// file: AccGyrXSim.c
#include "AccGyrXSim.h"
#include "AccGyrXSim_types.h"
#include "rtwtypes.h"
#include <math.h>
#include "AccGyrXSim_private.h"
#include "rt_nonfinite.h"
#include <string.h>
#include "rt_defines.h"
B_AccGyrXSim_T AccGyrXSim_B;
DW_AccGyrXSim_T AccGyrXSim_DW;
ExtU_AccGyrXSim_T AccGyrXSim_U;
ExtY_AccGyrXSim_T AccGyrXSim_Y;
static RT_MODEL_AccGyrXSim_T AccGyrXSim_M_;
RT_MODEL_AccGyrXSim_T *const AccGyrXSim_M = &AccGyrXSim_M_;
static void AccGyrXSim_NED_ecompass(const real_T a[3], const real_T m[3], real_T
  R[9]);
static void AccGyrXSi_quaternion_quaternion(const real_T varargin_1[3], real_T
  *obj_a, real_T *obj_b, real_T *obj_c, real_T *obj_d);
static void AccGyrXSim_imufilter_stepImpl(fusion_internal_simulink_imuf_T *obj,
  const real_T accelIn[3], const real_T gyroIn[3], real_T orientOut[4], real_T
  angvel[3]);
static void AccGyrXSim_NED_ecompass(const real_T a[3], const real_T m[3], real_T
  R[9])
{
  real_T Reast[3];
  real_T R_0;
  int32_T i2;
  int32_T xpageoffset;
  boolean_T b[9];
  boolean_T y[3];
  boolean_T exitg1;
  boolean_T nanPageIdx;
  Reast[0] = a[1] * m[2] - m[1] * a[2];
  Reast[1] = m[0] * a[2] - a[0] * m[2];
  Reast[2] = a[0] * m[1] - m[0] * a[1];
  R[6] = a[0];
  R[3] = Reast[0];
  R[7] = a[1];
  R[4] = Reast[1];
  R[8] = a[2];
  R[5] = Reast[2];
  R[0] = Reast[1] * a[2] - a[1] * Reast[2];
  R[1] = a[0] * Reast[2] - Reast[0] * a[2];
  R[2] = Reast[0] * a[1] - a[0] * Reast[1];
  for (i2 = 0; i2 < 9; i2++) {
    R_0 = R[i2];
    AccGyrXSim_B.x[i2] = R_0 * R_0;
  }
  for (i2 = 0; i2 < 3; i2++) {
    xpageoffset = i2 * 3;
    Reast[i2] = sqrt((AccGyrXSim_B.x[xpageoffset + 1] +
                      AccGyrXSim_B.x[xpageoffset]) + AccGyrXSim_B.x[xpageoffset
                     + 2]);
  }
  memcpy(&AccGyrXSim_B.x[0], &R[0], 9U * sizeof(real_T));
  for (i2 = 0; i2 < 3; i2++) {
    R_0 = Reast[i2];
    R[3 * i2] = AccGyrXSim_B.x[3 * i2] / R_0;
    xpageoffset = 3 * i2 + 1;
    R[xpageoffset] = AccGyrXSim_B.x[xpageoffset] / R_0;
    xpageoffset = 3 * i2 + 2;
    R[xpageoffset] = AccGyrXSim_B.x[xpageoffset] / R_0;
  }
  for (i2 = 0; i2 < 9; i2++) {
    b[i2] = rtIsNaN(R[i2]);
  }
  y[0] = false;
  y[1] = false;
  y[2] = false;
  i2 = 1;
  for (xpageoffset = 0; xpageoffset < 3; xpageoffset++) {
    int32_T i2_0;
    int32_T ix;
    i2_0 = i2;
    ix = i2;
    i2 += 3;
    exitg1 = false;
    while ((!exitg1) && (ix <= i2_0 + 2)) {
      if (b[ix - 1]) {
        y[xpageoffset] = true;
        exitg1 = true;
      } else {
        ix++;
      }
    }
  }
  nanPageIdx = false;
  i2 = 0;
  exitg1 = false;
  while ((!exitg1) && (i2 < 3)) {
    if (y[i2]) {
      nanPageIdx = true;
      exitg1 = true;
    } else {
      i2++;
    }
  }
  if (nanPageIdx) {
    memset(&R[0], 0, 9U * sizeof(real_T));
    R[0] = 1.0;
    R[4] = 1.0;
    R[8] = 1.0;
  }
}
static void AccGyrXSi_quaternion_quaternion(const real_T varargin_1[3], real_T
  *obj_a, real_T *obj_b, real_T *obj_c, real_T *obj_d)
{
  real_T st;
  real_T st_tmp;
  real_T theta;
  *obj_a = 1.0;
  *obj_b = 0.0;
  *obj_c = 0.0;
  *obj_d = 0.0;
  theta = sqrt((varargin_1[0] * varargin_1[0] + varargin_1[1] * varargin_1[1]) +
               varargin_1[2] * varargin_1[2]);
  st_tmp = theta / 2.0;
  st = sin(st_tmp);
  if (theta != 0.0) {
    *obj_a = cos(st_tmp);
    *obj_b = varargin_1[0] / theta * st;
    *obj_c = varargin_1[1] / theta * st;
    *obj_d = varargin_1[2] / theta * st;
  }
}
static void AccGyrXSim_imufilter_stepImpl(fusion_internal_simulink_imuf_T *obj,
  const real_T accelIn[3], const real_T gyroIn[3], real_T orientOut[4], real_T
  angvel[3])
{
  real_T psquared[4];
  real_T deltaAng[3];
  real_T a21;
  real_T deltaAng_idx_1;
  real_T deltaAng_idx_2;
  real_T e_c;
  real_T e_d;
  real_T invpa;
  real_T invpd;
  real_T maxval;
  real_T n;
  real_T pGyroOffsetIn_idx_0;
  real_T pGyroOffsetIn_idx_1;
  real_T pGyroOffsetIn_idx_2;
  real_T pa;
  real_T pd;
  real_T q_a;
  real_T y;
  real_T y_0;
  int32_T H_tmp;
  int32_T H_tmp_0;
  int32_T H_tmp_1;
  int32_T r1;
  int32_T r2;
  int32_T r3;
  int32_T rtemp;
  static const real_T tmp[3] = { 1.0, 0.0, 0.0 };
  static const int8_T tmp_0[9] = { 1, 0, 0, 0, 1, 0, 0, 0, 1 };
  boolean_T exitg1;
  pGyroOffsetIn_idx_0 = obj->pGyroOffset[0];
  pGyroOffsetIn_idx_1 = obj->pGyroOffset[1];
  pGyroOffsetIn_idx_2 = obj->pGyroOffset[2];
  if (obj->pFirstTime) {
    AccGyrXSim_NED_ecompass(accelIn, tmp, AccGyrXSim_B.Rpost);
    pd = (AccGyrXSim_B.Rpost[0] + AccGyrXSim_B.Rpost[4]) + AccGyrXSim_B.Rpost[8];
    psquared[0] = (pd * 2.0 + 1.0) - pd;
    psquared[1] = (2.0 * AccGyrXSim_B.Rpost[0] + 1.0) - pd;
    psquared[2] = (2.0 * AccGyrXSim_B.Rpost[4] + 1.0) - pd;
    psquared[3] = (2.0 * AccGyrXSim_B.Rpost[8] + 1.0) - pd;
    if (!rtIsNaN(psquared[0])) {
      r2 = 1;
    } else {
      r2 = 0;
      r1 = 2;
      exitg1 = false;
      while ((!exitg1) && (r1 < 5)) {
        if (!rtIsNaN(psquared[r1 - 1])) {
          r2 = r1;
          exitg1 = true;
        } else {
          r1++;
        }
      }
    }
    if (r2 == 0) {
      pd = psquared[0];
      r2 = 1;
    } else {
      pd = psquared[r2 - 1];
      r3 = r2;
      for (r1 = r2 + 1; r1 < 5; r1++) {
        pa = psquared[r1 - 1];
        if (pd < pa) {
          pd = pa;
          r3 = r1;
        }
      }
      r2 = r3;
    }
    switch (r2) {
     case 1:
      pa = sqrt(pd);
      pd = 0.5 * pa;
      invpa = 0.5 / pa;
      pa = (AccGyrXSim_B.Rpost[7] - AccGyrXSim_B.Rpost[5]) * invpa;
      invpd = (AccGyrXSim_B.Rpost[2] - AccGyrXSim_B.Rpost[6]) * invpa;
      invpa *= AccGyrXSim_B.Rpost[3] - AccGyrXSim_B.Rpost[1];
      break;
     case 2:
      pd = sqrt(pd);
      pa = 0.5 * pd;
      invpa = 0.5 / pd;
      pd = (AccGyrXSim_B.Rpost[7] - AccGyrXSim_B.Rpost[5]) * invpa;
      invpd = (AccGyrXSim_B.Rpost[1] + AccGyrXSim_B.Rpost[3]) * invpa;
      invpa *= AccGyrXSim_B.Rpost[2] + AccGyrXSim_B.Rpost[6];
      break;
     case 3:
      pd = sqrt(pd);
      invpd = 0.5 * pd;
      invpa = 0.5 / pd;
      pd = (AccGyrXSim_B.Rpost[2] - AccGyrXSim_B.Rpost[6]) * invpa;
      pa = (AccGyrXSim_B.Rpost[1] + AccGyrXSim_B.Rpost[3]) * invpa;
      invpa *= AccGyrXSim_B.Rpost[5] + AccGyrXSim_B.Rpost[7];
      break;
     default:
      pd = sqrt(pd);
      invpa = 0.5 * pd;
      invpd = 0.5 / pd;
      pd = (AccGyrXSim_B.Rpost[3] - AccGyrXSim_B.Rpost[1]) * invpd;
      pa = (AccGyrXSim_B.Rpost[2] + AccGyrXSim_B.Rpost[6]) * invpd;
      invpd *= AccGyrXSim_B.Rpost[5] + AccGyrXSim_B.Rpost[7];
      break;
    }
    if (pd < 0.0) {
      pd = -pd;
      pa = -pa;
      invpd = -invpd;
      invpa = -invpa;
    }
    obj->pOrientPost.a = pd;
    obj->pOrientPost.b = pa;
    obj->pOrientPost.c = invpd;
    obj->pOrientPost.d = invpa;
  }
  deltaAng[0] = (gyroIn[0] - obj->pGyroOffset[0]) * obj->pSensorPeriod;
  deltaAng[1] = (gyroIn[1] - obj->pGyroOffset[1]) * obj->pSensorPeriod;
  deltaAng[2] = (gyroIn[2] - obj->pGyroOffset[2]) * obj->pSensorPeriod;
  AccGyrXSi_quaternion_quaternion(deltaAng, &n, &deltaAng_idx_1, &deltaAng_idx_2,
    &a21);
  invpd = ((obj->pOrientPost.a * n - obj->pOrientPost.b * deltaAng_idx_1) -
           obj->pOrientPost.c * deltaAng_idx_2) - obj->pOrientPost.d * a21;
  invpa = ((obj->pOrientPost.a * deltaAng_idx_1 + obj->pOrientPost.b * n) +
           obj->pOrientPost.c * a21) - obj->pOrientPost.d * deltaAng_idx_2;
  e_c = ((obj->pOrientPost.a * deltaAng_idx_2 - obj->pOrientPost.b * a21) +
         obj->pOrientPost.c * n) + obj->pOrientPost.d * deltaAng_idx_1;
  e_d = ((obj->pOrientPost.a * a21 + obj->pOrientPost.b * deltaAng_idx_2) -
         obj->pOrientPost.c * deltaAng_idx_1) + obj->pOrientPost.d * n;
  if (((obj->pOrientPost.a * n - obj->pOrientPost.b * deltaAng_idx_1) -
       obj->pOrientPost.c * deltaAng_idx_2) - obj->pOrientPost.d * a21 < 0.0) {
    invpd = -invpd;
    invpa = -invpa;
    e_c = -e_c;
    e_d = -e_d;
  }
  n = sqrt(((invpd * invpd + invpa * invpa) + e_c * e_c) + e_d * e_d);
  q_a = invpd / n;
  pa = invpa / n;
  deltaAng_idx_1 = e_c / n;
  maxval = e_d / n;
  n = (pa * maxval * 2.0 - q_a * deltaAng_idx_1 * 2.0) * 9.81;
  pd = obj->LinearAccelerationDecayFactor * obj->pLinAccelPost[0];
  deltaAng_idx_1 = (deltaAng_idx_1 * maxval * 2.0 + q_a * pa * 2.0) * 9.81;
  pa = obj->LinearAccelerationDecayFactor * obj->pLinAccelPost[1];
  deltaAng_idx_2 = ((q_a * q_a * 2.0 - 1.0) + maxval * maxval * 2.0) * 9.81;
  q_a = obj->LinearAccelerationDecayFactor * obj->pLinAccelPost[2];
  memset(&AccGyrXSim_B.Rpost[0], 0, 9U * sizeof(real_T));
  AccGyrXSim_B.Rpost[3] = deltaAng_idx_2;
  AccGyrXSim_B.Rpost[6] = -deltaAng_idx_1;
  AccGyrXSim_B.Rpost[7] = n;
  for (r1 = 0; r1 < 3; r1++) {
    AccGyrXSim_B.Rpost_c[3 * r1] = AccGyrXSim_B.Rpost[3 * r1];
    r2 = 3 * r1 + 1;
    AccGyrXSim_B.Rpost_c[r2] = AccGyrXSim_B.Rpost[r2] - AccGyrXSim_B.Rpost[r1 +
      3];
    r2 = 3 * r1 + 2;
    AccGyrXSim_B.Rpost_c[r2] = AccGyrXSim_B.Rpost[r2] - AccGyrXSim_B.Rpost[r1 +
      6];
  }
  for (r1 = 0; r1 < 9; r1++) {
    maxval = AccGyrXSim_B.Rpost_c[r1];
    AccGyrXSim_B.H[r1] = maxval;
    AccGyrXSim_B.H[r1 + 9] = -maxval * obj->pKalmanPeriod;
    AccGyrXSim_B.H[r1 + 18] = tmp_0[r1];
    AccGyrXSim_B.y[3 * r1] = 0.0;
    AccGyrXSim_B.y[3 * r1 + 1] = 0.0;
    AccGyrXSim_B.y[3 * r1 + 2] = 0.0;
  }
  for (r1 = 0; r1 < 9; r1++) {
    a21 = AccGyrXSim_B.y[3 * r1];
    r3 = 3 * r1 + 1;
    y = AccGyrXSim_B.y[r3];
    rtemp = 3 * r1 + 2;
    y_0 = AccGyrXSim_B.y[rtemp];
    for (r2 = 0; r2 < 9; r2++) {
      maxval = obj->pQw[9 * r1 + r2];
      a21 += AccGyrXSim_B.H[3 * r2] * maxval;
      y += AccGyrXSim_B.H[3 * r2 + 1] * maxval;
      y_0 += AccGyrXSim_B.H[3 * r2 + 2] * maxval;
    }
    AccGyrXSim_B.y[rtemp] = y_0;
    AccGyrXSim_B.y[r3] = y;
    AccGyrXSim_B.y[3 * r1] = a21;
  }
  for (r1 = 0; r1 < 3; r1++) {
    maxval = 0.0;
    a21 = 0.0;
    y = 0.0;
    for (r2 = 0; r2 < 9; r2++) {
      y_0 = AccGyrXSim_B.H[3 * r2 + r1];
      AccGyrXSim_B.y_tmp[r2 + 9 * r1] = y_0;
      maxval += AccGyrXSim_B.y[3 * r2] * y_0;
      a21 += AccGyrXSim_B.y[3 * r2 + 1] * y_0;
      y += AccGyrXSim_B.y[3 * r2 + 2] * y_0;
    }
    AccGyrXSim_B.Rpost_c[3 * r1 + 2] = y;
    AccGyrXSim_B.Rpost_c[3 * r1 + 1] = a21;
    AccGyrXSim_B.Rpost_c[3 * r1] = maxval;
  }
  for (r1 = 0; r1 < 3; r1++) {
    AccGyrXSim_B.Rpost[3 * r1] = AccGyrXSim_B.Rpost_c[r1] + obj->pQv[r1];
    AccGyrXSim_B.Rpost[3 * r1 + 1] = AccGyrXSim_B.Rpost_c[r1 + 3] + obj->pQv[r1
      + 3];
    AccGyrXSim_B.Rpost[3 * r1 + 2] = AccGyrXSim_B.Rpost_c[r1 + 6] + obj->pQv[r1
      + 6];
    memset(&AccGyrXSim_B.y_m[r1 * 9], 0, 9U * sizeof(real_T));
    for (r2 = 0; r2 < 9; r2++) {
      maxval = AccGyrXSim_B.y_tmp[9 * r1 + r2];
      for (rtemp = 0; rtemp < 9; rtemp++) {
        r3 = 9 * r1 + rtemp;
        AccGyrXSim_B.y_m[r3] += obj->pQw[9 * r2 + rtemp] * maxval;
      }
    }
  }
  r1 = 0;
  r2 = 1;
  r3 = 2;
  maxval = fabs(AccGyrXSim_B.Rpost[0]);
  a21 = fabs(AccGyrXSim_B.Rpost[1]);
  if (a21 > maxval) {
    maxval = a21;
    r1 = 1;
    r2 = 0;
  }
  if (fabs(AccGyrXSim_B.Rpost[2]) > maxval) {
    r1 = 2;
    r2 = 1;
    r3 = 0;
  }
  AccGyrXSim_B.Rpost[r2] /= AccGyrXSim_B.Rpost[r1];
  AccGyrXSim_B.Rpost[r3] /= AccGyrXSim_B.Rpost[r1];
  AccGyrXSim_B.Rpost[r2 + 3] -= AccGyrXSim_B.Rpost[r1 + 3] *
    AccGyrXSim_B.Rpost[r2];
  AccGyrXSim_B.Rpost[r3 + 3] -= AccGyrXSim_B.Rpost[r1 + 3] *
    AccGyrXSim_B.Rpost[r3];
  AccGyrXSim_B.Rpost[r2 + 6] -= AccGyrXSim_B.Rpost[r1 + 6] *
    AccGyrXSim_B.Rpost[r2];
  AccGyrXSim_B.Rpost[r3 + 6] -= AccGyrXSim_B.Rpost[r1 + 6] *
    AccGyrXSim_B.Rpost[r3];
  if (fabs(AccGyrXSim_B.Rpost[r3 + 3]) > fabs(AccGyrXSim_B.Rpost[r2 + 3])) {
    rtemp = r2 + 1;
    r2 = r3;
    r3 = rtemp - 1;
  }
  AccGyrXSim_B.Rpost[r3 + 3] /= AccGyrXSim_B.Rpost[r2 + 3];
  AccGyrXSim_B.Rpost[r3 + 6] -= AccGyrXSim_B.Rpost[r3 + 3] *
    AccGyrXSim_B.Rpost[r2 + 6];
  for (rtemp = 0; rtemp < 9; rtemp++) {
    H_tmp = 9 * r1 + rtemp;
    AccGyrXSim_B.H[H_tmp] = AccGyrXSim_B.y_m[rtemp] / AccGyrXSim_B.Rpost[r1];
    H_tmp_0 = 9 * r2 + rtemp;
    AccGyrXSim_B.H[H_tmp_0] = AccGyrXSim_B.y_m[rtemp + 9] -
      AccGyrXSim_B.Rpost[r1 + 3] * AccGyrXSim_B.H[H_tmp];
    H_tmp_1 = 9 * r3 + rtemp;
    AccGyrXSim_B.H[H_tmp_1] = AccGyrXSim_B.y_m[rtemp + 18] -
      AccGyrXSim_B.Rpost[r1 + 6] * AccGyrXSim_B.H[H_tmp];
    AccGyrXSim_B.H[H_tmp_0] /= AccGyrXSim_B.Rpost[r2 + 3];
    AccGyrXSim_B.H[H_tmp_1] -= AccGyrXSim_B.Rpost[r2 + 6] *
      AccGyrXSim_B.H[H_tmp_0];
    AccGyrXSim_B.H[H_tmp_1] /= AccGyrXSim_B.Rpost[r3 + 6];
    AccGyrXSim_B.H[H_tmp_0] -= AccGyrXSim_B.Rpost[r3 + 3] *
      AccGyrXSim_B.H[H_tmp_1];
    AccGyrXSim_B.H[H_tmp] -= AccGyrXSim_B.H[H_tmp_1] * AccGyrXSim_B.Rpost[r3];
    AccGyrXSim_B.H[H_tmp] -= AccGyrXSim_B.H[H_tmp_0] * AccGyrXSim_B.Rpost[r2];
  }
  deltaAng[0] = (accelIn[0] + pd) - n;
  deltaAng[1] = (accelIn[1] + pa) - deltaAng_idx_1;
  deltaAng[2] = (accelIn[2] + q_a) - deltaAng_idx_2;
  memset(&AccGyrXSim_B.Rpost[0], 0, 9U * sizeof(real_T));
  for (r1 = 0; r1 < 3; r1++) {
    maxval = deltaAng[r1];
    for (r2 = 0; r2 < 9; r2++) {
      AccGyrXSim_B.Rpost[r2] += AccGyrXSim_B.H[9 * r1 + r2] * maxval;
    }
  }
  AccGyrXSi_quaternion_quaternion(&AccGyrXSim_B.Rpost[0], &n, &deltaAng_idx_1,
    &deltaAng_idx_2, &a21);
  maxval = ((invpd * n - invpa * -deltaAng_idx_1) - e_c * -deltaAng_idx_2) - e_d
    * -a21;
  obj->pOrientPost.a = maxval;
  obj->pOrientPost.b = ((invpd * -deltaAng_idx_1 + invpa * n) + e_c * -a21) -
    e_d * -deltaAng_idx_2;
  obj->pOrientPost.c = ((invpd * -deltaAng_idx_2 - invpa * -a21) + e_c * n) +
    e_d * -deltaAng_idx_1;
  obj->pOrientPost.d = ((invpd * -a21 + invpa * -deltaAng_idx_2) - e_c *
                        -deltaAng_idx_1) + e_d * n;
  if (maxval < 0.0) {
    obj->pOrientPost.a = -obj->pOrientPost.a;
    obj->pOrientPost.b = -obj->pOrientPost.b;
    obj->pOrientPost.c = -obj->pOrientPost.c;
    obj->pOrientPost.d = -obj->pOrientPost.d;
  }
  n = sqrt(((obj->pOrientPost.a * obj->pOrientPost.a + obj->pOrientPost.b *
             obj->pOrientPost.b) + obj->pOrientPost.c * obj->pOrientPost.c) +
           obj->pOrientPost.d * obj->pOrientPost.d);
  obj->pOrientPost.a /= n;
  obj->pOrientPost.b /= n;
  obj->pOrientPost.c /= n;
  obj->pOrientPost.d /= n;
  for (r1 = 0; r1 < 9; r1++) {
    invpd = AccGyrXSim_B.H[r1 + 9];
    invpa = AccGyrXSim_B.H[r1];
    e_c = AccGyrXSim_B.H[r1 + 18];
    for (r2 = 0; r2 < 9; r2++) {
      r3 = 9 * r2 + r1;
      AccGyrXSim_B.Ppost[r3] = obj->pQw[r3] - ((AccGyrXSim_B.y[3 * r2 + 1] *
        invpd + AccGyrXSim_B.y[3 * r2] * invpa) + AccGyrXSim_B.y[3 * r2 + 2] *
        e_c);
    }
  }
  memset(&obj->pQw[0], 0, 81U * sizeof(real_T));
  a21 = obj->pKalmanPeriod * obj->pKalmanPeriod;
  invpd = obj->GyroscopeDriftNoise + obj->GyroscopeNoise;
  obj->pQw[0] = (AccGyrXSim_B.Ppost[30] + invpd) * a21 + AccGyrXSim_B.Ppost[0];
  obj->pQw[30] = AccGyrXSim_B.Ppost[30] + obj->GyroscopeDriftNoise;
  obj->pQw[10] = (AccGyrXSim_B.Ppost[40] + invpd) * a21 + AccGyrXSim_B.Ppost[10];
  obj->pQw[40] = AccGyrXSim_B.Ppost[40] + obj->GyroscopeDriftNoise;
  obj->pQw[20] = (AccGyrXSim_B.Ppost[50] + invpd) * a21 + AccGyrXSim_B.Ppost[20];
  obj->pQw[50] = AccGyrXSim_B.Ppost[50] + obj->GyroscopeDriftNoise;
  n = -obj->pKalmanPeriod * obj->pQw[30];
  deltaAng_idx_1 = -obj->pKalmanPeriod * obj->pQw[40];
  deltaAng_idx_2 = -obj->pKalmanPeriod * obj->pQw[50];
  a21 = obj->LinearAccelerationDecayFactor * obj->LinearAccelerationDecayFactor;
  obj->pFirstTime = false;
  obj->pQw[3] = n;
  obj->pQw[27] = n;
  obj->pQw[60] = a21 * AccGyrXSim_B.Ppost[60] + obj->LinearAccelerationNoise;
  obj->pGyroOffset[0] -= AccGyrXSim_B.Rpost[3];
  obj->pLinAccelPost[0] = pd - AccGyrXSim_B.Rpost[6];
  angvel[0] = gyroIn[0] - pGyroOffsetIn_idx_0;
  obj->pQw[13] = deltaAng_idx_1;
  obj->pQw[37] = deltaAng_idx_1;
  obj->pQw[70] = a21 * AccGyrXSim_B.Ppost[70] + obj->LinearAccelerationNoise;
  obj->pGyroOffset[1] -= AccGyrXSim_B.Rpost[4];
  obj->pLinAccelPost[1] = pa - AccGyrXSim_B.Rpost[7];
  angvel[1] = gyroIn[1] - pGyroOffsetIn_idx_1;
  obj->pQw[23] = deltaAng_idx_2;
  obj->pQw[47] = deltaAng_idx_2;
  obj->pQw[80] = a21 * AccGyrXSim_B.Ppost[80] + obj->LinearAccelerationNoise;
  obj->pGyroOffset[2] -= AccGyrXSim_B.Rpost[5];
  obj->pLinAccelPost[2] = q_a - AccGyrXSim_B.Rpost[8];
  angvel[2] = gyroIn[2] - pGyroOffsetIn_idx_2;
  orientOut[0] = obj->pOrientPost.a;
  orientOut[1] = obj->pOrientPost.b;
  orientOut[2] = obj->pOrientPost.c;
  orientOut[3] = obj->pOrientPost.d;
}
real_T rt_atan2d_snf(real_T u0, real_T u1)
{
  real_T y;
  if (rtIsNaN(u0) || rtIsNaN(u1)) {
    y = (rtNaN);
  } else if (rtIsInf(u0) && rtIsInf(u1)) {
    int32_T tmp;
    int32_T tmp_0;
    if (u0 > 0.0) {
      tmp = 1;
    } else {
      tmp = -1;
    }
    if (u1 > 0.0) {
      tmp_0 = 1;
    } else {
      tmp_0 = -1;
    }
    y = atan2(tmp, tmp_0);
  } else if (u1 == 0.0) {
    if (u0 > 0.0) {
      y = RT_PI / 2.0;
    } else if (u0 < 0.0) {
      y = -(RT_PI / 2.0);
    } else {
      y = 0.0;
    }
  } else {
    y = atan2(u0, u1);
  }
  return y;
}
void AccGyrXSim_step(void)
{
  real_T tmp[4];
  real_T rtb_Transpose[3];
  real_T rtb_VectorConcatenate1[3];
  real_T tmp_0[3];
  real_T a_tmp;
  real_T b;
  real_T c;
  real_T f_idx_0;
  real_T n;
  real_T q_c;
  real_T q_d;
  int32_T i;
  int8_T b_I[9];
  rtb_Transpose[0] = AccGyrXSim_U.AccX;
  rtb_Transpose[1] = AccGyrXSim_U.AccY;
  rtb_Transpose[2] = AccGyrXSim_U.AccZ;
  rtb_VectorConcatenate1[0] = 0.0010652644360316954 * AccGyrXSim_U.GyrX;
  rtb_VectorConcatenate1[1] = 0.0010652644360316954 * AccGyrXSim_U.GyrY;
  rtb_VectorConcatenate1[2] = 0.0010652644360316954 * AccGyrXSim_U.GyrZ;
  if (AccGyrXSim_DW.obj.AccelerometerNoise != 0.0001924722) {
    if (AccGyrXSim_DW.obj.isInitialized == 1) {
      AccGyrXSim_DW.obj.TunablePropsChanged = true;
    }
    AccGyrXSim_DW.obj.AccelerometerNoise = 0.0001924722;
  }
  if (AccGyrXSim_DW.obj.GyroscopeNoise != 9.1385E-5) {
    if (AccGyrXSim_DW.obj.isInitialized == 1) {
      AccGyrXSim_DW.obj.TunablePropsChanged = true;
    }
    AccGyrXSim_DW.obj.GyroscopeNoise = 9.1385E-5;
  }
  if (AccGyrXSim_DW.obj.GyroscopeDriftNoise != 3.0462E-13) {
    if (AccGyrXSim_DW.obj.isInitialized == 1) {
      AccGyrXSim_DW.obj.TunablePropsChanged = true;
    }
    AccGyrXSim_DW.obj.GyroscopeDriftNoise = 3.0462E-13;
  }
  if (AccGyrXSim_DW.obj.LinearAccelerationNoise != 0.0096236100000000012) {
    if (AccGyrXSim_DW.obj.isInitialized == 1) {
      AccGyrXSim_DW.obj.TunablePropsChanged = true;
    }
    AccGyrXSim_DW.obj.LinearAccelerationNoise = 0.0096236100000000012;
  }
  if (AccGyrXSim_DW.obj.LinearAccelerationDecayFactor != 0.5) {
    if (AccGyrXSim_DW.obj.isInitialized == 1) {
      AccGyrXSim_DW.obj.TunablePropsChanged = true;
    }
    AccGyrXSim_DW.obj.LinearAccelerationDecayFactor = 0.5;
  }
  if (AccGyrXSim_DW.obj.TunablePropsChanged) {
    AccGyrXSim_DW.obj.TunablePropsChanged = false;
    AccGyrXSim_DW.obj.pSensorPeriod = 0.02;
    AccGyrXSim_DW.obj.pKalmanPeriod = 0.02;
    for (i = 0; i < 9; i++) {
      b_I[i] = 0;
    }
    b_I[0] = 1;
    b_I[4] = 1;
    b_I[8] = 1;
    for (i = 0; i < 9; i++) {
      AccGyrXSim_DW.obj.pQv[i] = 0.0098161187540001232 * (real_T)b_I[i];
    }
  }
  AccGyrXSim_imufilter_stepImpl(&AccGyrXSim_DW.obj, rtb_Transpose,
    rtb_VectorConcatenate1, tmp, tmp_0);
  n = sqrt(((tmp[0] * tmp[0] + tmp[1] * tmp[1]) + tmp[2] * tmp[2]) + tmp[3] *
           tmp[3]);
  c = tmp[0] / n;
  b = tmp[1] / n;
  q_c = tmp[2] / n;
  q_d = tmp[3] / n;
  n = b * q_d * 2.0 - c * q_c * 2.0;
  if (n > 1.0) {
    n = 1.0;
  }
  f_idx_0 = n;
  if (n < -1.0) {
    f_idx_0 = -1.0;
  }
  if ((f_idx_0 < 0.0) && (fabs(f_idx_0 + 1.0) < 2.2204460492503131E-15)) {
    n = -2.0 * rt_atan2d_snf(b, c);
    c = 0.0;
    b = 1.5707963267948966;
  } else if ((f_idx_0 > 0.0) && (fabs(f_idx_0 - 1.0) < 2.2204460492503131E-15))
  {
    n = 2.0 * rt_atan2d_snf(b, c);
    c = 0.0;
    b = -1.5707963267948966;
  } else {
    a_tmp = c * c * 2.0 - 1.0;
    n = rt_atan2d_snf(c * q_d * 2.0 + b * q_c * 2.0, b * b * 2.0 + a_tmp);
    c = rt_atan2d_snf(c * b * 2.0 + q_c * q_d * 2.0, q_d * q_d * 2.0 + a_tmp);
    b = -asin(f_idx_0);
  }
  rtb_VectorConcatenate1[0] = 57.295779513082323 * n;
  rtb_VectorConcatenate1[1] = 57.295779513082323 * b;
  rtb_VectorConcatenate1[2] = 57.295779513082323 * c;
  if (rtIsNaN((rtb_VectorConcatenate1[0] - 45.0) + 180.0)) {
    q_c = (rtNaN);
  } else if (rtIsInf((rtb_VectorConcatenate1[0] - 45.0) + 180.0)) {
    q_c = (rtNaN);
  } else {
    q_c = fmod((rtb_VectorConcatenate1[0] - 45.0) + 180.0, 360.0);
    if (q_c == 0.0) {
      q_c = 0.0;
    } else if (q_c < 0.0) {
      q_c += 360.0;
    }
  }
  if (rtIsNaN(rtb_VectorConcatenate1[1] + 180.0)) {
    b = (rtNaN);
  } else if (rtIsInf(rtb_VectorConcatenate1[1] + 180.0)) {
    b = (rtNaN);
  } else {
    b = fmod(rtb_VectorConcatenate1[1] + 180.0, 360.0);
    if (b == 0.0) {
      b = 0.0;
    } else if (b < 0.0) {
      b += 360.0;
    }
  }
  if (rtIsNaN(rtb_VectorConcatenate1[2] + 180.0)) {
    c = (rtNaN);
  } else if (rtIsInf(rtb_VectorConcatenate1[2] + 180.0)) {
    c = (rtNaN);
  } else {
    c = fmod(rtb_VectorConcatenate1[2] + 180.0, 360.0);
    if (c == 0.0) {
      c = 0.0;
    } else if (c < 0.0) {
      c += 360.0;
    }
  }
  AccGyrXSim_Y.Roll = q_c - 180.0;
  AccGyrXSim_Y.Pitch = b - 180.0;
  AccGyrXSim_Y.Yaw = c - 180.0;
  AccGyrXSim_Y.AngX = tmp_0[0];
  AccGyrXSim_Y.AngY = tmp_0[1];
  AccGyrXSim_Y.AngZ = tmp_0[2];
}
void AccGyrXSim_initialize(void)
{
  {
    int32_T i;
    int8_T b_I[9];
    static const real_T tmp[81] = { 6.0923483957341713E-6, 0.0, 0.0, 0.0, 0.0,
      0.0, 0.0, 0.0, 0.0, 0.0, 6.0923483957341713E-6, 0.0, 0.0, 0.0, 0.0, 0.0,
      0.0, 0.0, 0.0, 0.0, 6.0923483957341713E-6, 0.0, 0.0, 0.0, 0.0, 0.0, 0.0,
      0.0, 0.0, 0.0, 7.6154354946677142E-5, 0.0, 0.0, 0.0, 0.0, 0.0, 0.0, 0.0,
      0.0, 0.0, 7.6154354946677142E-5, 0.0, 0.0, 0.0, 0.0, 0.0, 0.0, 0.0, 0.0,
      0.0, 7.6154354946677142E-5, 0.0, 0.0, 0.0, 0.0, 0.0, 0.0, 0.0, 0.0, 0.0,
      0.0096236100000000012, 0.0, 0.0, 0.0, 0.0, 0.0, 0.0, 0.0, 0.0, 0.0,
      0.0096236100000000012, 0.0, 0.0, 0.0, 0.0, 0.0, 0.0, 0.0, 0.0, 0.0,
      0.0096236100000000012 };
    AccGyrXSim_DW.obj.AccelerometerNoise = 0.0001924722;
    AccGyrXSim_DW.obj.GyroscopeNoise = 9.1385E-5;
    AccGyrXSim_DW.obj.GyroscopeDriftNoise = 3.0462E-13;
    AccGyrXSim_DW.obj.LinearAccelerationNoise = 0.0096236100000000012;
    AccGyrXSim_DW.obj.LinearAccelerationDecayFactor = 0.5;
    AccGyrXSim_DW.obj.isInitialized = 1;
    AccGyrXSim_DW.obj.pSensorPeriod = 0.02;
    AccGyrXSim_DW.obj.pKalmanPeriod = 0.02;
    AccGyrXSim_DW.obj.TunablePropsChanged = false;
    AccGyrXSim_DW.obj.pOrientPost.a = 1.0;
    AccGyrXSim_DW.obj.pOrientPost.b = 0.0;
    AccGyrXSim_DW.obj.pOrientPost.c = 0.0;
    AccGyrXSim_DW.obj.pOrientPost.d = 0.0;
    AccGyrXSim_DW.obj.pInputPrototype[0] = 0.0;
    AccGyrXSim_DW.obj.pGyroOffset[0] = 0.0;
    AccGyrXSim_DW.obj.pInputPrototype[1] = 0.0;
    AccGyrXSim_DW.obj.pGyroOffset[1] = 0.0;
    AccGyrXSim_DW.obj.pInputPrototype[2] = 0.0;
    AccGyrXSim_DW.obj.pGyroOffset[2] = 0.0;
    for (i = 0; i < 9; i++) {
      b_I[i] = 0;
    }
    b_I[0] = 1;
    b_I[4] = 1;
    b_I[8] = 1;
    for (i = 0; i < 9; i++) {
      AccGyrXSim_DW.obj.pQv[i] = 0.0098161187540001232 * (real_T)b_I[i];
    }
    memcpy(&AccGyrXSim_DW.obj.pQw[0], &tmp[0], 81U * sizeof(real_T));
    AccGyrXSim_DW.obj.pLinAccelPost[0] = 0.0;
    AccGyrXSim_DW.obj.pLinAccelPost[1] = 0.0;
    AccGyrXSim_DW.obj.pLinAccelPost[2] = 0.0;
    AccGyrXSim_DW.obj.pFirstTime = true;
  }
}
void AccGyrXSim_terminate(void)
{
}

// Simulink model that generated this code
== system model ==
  AccX : Inport
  AccY : Inport
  AccZ : Inport
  GyrX : Inport
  GyrY : Inport
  GyrZ : Inport
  Roll : Outport  <- 1: MATLABFunction#1
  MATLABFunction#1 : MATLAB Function  <- 1: IMUFilter#1
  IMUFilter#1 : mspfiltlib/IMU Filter  <- 1: Transpose, 2: Math#1
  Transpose : Math  Operator=transpose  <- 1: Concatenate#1
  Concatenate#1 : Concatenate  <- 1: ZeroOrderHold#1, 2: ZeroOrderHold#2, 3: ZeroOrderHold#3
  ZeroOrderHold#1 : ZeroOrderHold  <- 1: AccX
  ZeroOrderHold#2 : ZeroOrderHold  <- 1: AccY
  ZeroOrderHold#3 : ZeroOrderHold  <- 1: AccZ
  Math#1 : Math  Operator=transpose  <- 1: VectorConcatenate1
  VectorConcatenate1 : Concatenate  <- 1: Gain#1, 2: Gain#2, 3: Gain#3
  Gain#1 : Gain  Gain=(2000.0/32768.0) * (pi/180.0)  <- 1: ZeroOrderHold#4
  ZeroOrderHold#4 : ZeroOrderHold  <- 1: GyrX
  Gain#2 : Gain  Gain=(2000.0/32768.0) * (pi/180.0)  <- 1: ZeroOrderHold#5
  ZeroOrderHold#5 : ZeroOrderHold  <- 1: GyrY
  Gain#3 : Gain  Gain=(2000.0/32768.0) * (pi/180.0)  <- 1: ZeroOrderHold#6
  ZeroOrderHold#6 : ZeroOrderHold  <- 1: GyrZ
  Pitch : Outport  <- 1: MATLABFunction#1/2
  Yaw : Outport  <- 1: MATLABFunction#1/3
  AngX : Outport  <- 1: MATLABFunction#2
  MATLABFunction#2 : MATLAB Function  <- 1: IMUFilter#1/2
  AngY : Outport  <- 1: MATLABFunction#2/2
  AngZ : Outport  <- 1: MATLABFunction#2/3
== matlab function MATLABFunction#2 ==
function [AngX,AngY,AngZ] = fcn(u)

y = u;
AngX = y(1);
AngY = y(2);
AngZ = y(3);

== matlab function MATLABFunction#1 ==
function [roll, pitch, yaw] = hquat2eul(u)

q2 = quaternion(u(:,1), u(:,2), u(:,3), u(:,4));
y = eulerd(q2, "ZYX", "frame");

yaw = y(3);
pitch = y(2);
roll = y(1)-45;

roll  = mod(roll  + 180, 360) - 180;
pitch = mod(pitch + 180, 360) - 180;
yaw   = mod(yaw   + 180, 360) - 180;
